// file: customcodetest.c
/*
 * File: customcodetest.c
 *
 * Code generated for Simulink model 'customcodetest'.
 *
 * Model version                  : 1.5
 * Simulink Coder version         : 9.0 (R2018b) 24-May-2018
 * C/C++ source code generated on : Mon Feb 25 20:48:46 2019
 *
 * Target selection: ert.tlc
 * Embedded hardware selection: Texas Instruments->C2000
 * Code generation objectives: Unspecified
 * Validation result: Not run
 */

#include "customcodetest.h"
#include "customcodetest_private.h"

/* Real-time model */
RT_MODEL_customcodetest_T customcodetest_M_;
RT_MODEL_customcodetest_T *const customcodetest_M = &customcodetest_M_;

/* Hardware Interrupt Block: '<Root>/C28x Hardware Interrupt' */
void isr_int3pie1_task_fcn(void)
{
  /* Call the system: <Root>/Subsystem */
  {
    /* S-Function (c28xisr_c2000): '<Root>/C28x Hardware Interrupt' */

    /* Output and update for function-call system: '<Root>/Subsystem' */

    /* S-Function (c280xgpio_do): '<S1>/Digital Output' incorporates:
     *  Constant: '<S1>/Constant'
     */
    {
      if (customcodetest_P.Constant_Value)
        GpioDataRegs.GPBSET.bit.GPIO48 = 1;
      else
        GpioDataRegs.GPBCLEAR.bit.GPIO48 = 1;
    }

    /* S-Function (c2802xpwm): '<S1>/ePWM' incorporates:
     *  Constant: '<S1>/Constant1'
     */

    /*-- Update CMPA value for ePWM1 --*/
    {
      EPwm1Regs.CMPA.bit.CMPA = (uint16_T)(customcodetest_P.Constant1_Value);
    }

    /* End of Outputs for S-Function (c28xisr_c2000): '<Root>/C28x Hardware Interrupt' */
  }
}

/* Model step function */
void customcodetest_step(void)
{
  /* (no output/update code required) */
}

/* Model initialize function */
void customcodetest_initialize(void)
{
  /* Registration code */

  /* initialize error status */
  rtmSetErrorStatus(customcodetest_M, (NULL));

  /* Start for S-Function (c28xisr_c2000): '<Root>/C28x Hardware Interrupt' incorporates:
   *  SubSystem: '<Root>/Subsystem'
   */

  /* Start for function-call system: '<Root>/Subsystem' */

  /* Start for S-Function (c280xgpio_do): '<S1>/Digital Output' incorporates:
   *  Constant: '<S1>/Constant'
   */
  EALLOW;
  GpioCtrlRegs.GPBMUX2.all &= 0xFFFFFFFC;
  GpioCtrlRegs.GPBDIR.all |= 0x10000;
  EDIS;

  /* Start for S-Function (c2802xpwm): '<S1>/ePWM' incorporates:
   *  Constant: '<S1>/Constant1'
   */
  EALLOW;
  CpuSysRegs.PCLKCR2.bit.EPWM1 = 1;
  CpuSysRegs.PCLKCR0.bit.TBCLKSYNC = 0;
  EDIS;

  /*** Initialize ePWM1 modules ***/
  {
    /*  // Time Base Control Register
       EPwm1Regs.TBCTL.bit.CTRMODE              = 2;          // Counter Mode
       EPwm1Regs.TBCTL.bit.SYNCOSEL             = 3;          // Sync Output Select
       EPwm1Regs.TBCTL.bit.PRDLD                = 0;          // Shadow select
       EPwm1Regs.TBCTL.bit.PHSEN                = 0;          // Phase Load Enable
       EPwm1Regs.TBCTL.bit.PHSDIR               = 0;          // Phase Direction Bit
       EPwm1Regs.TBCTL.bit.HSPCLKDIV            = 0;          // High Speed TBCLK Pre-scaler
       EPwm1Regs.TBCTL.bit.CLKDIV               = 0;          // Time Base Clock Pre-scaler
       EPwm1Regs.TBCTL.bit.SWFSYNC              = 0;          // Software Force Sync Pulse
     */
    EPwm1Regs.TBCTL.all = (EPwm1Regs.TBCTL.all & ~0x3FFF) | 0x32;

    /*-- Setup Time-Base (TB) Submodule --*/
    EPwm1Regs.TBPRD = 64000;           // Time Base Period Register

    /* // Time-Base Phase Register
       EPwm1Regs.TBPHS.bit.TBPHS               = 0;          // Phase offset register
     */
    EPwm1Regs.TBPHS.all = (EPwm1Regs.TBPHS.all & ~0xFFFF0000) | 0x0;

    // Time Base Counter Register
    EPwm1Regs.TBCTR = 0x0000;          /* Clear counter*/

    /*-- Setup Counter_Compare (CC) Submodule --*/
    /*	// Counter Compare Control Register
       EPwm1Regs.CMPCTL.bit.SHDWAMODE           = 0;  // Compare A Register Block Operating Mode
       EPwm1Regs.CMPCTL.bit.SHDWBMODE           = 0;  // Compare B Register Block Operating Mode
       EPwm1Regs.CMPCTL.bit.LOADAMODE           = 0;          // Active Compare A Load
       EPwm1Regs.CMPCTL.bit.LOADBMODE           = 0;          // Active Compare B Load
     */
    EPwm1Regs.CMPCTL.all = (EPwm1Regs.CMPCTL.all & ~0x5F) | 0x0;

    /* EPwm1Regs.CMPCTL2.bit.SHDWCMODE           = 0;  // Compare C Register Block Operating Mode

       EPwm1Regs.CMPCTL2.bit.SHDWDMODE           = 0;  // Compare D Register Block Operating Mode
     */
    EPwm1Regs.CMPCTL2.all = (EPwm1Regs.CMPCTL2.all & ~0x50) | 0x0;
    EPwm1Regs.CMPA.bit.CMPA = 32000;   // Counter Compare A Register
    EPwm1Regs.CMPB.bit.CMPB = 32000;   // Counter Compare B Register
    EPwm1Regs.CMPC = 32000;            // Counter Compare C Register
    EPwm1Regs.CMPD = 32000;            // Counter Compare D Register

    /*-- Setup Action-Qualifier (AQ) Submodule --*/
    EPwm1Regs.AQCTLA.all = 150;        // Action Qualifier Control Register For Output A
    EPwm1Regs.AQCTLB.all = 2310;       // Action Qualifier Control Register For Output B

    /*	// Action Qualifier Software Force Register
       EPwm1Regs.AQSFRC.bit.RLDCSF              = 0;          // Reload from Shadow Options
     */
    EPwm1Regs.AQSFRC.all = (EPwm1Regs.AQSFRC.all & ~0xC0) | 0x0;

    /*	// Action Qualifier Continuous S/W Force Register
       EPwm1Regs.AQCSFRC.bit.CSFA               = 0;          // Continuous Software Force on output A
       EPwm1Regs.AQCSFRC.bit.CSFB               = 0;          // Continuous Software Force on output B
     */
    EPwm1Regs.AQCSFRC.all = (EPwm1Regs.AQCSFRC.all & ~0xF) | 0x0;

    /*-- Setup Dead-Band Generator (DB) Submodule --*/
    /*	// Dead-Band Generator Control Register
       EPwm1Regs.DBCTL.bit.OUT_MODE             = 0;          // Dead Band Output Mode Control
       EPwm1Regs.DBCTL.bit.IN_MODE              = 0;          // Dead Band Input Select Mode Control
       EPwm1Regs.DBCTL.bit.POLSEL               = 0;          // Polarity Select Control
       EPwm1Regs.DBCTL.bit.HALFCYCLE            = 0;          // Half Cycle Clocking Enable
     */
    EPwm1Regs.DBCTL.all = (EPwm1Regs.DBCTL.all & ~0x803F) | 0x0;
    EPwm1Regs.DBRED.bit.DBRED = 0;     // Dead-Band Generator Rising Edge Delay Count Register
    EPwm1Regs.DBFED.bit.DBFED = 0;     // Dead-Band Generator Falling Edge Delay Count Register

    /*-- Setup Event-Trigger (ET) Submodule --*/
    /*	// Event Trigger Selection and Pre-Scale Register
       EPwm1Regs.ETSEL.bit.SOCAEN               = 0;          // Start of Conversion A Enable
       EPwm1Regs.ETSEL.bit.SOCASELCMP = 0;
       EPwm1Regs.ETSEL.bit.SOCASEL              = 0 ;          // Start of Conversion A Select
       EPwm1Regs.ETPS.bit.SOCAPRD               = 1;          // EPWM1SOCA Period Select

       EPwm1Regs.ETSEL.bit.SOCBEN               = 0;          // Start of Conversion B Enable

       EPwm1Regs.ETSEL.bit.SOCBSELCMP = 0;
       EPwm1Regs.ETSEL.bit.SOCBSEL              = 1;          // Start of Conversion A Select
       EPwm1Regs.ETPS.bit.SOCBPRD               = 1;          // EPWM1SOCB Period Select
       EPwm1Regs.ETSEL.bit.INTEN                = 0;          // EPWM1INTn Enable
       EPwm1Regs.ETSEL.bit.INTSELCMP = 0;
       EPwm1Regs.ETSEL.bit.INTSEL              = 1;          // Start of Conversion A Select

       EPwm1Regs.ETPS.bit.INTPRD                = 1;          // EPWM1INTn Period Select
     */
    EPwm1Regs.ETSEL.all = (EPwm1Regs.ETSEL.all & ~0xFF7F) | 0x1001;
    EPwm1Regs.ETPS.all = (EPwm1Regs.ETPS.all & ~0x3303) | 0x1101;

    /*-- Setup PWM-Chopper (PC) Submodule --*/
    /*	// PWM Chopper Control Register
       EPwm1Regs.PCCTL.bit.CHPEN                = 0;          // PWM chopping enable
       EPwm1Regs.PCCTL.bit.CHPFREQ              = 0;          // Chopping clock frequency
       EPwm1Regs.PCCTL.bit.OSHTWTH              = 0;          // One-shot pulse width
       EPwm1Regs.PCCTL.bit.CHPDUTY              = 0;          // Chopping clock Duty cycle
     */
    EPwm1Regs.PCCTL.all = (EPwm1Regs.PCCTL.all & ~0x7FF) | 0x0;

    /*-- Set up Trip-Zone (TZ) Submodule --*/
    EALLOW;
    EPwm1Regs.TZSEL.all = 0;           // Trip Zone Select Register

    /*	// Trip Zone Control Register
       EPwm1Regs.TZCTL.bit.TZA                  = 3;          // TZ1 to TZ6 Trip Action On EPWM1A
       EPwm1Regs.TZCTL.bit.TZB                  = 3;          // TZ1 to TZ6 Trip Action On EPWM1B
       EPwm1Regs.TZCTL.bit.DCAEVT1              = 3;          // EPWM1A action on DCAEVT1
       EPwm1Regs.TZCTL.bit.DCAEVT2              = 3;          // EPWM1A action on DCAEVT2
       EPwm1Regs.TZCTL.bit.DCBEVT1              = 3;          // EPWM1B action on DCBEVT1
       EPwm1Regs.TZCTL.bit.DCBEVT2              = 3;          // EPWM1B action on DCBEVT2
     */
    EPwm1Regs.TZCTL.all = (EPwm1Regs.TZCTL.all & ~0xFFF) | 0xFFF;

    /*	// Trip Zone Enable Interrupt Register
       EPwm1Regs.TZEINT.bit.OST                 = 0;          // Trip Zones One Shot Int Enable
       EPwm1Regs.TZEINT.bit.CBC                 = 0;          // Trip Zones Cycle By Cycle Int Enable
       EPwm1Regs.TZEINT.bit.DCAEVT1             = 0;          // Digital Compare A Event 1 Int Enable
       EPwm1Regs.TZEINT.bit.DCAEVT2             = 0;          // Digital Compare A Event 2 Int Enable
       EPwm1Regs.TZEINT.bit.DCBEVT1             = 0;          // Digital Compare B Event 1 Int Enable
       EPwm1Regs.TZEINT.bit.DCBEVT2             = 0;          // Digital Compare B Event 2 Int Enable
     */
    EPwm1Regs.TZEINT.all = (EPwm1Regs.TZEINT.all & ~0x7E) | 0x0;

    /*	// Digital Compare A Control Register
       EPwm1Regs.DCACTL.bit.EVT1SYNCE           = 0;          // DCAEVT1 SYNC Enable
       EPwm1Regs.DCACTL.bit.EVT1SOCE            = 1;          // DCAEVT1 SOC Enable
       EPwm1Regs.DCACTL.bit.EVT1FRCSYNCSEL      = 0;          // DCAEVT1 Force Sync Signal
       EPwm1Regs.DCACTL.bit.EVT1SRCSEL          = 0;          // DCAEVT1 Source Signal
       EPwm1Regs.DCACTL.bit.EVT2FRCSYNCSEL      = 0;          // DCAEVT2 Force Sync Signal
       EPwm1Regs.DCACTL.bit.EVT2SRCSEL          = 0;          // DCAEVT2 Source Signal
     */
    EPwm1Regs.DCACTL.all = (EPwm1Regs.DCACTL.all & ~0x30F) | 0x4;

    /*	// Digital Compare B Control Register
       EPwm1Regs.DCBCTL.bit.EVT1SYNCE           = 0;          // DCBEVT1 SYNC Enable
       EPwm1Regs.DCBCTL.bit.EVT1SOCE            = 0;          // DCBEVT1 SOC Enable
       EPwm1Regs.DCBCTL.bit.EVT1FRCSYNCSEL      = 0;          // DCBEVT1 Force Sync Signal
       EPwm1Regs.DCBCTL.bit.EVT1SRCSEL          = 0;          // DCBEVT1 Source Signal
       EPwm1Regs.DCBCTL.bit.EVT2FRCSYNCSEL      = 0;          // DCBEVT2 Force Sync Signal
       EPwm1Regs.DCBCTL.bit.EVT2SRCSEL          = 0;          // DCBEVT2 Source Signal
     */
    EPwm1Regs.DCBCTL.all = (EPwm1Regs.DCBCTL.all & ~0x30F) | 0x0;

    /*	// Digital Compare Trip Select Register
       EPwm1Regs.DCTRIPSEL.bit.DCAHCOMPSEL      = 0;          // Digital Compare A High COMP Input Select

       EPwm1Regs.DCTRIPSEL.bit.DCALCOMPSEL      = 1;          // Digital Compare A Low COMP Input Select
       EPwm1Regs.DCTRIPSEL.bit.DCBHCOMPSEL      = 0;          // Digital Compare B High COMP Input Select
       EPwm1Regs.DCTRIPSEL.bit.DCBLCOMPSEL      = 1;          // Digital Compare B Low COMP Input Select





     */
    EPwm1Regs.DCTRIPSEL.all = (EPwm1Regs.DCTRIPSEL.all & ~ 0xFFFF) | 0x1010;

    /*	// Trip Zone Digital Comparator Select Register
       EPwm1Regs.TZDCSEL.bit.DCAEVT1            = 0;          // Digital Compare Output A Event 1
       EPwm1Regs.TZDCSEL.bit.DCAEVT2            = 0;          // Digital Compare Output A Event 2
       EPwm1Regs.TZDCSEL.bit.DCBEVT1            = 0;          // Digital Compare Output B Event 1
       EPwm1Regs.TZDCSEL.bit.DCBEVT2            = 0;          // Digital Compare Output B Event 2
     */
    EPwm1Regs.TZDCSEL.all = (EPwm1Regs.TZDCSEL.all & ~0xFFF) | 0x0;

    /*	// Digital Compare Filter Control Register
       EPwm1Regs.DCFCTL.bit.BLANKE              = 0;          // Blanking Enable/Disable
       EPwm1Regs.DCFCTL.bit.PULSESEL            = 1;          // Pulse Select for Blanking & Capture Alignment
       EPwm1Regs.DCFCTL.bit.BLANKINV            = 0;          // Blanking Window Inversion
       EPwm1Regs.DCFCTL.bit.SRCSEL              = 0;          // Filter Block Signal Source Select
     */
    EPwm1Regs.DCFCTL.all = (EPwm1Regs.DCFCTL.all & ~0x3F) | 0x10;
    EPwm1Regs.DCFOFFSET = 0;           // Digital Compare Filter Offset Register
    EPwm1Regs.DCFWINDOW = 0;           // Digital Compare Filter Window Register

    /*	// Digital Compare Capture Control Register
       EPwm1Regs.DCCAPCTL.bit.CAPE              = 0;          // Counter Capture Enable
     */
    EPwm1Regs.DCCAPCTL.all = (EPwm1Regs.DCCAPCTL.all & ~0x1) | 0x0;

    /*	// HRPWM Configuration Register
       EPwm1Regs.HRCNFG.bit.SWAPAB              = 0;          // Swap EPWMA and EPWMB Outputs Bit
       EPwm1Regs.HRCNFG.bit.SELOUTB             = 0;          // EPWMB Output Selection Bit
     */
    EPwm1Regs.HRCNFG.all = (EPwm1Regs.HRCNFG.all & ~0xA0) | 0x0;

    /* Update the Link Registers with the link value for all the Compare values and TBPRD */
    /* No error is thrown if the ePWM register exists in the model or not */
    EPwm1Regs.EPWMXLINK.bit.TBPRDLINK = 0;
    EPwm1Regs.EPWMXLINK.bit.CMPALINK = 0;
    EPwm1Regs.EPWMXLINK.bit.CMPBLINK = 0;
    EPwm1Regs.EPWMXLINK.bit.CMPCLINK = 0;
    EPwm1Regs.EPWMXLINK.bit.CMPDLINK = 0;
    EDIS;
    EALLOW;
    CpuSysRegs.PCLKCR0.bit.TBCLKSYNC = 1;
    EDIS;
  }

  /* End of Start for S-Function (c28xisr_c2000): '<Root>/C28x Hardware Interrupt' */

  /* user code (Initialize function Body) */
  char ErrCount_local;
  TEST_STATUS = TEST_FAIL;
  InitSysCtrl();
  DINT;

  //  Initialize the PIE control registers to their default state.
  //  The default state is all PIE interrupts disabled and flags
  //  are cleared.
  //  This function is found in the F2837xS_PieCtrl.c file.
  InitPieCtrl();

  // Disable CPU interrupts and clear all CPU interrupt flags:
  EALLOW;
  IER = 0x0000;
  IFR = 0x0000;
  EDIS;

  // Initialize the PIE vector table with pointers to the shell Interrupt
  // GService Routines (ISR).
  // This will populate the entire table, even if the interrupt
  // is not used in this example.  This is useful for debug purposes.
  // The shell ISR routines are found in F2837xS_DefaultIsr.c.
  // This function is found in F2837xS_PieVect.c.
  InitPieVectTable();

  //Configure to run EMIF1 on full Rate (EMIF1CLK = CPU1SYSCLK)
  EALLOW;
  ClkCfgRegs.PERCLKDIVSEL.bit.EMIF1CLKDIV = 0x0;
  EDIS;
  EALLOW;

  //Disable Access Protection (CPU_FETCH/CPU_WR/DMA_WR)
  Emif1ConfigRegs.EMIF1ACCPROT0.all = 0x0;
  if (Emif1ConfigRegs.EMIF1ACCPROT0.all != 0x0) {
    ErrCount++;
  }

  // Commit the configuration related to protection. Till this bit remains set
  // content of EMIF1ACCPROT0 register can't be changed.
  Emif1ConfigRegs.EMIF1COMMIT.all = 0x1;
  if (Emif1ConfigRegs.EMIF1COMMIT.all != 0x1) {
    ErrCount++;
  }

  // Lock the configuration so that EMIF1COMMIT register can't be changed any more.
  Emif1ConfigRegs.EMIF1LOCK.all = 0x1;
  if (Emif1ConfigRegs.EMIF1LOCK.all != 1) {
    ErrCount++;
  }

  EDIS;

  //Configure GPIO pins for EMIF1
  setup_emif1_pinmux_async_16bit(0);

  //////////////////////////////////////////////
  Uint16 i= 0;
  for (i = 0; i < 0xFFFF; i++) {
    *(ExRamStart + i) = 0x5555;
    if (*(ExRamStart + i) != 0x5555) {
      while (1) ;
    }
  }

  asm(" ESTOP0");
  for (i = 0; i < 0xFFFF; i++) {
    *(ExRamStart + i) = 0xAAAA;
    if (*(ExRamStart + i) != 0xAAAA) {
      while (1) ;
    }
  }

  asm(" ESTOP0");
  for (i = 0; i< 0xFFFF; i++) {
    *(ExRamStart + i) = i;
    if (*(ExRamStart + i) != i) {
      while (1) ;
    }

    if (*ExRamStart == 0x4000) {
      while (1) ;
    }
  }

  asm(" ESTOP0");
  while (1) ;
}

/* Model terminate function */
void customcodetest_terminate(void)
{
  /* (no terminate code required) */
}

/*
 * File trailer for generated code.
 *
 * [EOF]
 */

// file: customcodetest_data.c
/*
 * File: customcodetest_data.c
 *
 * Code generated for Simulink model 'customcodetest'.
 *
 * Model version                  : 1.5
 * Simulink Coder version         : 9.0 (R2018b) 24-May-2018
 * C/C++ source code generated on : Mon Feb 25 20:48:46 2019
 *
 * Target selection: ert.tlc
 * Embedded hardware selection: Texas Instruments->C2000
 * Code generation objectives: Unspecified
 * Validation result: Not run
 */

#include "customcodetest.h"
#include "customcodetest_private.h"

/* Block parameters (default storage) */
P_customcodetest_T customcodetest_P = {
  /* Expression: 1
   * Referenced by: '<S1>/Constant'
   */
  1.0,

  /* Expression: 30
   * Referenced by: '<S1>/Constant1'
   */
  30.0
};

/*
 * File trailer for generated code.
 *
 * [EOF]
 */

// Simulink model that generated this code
simulink model "customcodetest"  (R2018b)
settings: Solver=FixedStepDiscrete  StartTime=0.0  StopTime=Inf  RelTol=1e-3  EnableMultiTasking=on
undefined symbols (not defined in the file or in its folder): Down, GPTRIP1SEL, GPTRIP2SEL, TZ1, TZ2, Up
libraries: c2000lib x1, c2837xDlib x1, c2802xlib x1

== system customcodetest ==
  C28x Hardware Interrupt : c2000lib/Scheduling/C28x Hardware Interrupt  irqnumbers=[3]  pienumbers=[1]  irqpriorities=[30]  irqpreempts=[0]  showinput=off  dspchiptype=C280X
  Subsystem : Subsystem
  wires:
  C28x Hardware Interrupt/1 -> Subsystem/Trigger

== system customcodetest/Subsystem ==
  function : TriggerPort  TriggerType=function-call  VariantControl=(inherit)  SampleTime=1e-5
  Constant : Constant
  Constant1 : Constant  Value=30
  Digital Output : c2837xDlib/Digital Output  GPIO_Number=GPIO48~GPIO55  GPIO_Bit0=on  GPIO_BIT0_Toggle=off  GPIO_Bit1=off  GPIO_BIT1_Toggle=off  GPIO_Bit2=off  GPIO_BIT2_Toggle=off  GPIO_Bit3=off  GPIO_BIT3_Toggle=on  GPIO_Bit4=off  GPIO_BIT4_Toggle=off  GPIO_Bit5=off  GPIO_BIT5_Toggle=off  GPIO_Bit6=off  GPIO_BIT6_Toggle=off  GPIO_Bit7=off  GPIO_BIT7_Toggle=off
  ePWM : c2802xlib/ePWM  useModule=ePWM1  ePWMxLINKTBPRD=Not Linked  periodUnits=Clock cycles  timerSource=Specify via dialog  timerPeriod_clk=64000  timerPeriod_sec=0.0001  tbshadow=Counter equals to zero  countingMode=Up-Down  phaseActiveEnable=Disable  phaseDirection=Count down after sync  phaseActive=0  synchronizationEnable=off  dcaevt1Sync=off  dcbevt1Sync=off  synchronizationOption=Disable  clockPrescale=1  HSclockPrescale=1  enswap=off  ePWMxAStatus=on  ePWMxAactionLogic1=Set  ePWMxAactionLogic2=Clear  ePWMxAactionLogic3=Clear  ePWMxAactionLogic4=Set  ePWMxAactionLogic5=Do nothing  ePWMxAactionLogic6=Do nothing  ePWMxALoadMode=Load on counter equals to zero (CTR=Zero)  ePWMxACSFenable=off  ePWMxACSFvalue=Forcing disable  ePWMxASFreload=Zero  ePWMxBStatus=off  ePWMxBactionLogic1=Set  ePWMxBactionLogic2=Clear  ePWMxBactionLogic3=Do nothing  ePWMxBactionLogic4=Do nothing  ePWMxBactionLogic5=Clear  ePWMxBactionLogic6=Set  ePWMxBLoadMode=Load on counter equals to zero (CTR=Zero)  ePWMxBCSFenable=off  ePWMxBCSFvalue=Forcing disable  ePWMxBSFreload=Zero  ePWNxBOutWay=off  ePWMxLINKCMPA=Not Linked  CMPAUnits=Clock cycles  CMPASource=Input port  CMPAValue_per=50  CMPAValue_clk=32000  enCMPAshadow=Counter equals to zero  ePWMxLINKCMPB=Not Linked  CMPBUnits=Clock cycles  CMPBSource=Specify via dialog  CMPBValue_per=50  CMPBValue_clk=32000  enCMPBshadow=Counter equals to zero  ePWMxLINKCMPC=Not Linked  CMPCUnits=Clock cycles  CMPCSource=Specify via dialog  CMPCValue_per=50  CMPCValue_clk=32000  enCMPCshadow=Counter equals to zero  ePWMxLINKCMPD=Not Linked  CMPDUnits=Clock cycles  CMPDSource=Specify via dialog  CMPDValue_per=50  CMPDValue_clk=32000  enCMPDshadow=Counter equals to zero  enableDBePWMxA=off  enableDBePWMxB=off  enhalfcycle=off  DBpolarity=Active high (AH)  DBedgeDelay=Positive  DBSource_ePWMxA=ePWMxA  DBSource_ePWMxB=ePWMxA  DBperiodSource=Specify via dialog  REDperiod=0  FEDperiod=0  adcstartModuleA=off  adcrequestEventA=First event  adcstartEventA=Digital Compare Module A Event 1 start of conversion (DCAEVT1.soc)  adcstartEventA_type2=Digital Compare Module A Event 1 start of conversion (DCAEVT1.soc)  adcstartModuleB=off  adcrequestEventB=First event  adcstartEventB=Counter equals to zero (CTR=Zero)  adcstartEventB_type2=Counter equals to zero (CTR=Zero)  intEn=off  intPrd=First event  intSel=Counter equals to zero (CTR=Zero)  intSel_type2=Counter equals to zero (CTR=Zero)  hrpe=off  enHRPWM=off  HRPWM_LoadMode=Counter equals to period (CTR=PRD)  HRPWM_CTLMode=Duty or Period control mode  HRPWM_EDGMode=Both edge  hrpeb=off  enHRPWMB=off  HRPWM_LoadModeB=Counter equals to zero (CTR=ZERO)  HRPWM_CTLModeB=Duty or Period control mode  HRPWM_EDGModeB=Both edge  enSFO=on  enautoconv=on  chopperEnable=off  chopperFrequency=1  chopperFirstwidth=1  chopperDuty=12.5%  tripZonesource=Specify via dialog  tzselOSHT1=off  tzselOSHT2=off  tzselOSHT3=off  tzselOSHDCAEV1=off  tzselOSHDCBEV1=off  tzselCBC1=off  tzselCBC2=off  tzselCBC3=off  tzselCBCDCAEV2=off  tzselCBCDCBEV2=off  tzselOSHT4=off  tzselOSHT5=off  tzselOSHT6=off  tzselCBC4=off  tzselCBC5=off  tzselCBC6=off  enTzOstIntr=off  enTzCbcIntr=off  enTzDCAEVT1Intr=off  enTzDCAEVT2Intr=off  enTzDCBEVT1Intr=off  enTzDCBEVT2Intr=off  ePWMxAforced=No action  ePWMxBforced=No action  DCAEVT1forced=No action  DCBEVT1forced=No action  DCAEVT2forced=No action  DCBEVT2forced=No action  dcah=Trip Zone 1 input (TZ1)  dcal=Trip Zone 2 input (TZ2)  dcbh=Trip Zone 1 input (TZ1)  dcbl=Trip Zone 2 input (TZ2)  dcah_type2=GPTRIP1SEL/(TZ1)  dcal_type2=GPTRIP2SEL/(TZ2)  dcbh_type2=GPTRIP1SEL/(TZ1)  dcbl_type2=GPTRIP2SEL/(TZ2)  gendcaevt1=Event disabled  gendcaevt2=Event disabled  gendcbevt1=Event disabled  gendcbevt2=Event disabled  dcaevt1src=DCAEVT1 with sync  dcaevt2src=DCAEVT2 with sync  dcbevt1src=DCBEVT1 with sync  dcbevt2src=DCBEVT2 with sync  pulsesel=Counter equals to zero (CTR=Zero)  blankinv=off  blankoffset=0  blankwidth=0  evsrcsel=Filtered version of DCAEVT1 (DCAEVT1FILT)  encape=off  PwmType=C2000_Type4
  wires:
  Constant/1 -> Digital Output/1
  Constant1/1 -> ePWM/1
